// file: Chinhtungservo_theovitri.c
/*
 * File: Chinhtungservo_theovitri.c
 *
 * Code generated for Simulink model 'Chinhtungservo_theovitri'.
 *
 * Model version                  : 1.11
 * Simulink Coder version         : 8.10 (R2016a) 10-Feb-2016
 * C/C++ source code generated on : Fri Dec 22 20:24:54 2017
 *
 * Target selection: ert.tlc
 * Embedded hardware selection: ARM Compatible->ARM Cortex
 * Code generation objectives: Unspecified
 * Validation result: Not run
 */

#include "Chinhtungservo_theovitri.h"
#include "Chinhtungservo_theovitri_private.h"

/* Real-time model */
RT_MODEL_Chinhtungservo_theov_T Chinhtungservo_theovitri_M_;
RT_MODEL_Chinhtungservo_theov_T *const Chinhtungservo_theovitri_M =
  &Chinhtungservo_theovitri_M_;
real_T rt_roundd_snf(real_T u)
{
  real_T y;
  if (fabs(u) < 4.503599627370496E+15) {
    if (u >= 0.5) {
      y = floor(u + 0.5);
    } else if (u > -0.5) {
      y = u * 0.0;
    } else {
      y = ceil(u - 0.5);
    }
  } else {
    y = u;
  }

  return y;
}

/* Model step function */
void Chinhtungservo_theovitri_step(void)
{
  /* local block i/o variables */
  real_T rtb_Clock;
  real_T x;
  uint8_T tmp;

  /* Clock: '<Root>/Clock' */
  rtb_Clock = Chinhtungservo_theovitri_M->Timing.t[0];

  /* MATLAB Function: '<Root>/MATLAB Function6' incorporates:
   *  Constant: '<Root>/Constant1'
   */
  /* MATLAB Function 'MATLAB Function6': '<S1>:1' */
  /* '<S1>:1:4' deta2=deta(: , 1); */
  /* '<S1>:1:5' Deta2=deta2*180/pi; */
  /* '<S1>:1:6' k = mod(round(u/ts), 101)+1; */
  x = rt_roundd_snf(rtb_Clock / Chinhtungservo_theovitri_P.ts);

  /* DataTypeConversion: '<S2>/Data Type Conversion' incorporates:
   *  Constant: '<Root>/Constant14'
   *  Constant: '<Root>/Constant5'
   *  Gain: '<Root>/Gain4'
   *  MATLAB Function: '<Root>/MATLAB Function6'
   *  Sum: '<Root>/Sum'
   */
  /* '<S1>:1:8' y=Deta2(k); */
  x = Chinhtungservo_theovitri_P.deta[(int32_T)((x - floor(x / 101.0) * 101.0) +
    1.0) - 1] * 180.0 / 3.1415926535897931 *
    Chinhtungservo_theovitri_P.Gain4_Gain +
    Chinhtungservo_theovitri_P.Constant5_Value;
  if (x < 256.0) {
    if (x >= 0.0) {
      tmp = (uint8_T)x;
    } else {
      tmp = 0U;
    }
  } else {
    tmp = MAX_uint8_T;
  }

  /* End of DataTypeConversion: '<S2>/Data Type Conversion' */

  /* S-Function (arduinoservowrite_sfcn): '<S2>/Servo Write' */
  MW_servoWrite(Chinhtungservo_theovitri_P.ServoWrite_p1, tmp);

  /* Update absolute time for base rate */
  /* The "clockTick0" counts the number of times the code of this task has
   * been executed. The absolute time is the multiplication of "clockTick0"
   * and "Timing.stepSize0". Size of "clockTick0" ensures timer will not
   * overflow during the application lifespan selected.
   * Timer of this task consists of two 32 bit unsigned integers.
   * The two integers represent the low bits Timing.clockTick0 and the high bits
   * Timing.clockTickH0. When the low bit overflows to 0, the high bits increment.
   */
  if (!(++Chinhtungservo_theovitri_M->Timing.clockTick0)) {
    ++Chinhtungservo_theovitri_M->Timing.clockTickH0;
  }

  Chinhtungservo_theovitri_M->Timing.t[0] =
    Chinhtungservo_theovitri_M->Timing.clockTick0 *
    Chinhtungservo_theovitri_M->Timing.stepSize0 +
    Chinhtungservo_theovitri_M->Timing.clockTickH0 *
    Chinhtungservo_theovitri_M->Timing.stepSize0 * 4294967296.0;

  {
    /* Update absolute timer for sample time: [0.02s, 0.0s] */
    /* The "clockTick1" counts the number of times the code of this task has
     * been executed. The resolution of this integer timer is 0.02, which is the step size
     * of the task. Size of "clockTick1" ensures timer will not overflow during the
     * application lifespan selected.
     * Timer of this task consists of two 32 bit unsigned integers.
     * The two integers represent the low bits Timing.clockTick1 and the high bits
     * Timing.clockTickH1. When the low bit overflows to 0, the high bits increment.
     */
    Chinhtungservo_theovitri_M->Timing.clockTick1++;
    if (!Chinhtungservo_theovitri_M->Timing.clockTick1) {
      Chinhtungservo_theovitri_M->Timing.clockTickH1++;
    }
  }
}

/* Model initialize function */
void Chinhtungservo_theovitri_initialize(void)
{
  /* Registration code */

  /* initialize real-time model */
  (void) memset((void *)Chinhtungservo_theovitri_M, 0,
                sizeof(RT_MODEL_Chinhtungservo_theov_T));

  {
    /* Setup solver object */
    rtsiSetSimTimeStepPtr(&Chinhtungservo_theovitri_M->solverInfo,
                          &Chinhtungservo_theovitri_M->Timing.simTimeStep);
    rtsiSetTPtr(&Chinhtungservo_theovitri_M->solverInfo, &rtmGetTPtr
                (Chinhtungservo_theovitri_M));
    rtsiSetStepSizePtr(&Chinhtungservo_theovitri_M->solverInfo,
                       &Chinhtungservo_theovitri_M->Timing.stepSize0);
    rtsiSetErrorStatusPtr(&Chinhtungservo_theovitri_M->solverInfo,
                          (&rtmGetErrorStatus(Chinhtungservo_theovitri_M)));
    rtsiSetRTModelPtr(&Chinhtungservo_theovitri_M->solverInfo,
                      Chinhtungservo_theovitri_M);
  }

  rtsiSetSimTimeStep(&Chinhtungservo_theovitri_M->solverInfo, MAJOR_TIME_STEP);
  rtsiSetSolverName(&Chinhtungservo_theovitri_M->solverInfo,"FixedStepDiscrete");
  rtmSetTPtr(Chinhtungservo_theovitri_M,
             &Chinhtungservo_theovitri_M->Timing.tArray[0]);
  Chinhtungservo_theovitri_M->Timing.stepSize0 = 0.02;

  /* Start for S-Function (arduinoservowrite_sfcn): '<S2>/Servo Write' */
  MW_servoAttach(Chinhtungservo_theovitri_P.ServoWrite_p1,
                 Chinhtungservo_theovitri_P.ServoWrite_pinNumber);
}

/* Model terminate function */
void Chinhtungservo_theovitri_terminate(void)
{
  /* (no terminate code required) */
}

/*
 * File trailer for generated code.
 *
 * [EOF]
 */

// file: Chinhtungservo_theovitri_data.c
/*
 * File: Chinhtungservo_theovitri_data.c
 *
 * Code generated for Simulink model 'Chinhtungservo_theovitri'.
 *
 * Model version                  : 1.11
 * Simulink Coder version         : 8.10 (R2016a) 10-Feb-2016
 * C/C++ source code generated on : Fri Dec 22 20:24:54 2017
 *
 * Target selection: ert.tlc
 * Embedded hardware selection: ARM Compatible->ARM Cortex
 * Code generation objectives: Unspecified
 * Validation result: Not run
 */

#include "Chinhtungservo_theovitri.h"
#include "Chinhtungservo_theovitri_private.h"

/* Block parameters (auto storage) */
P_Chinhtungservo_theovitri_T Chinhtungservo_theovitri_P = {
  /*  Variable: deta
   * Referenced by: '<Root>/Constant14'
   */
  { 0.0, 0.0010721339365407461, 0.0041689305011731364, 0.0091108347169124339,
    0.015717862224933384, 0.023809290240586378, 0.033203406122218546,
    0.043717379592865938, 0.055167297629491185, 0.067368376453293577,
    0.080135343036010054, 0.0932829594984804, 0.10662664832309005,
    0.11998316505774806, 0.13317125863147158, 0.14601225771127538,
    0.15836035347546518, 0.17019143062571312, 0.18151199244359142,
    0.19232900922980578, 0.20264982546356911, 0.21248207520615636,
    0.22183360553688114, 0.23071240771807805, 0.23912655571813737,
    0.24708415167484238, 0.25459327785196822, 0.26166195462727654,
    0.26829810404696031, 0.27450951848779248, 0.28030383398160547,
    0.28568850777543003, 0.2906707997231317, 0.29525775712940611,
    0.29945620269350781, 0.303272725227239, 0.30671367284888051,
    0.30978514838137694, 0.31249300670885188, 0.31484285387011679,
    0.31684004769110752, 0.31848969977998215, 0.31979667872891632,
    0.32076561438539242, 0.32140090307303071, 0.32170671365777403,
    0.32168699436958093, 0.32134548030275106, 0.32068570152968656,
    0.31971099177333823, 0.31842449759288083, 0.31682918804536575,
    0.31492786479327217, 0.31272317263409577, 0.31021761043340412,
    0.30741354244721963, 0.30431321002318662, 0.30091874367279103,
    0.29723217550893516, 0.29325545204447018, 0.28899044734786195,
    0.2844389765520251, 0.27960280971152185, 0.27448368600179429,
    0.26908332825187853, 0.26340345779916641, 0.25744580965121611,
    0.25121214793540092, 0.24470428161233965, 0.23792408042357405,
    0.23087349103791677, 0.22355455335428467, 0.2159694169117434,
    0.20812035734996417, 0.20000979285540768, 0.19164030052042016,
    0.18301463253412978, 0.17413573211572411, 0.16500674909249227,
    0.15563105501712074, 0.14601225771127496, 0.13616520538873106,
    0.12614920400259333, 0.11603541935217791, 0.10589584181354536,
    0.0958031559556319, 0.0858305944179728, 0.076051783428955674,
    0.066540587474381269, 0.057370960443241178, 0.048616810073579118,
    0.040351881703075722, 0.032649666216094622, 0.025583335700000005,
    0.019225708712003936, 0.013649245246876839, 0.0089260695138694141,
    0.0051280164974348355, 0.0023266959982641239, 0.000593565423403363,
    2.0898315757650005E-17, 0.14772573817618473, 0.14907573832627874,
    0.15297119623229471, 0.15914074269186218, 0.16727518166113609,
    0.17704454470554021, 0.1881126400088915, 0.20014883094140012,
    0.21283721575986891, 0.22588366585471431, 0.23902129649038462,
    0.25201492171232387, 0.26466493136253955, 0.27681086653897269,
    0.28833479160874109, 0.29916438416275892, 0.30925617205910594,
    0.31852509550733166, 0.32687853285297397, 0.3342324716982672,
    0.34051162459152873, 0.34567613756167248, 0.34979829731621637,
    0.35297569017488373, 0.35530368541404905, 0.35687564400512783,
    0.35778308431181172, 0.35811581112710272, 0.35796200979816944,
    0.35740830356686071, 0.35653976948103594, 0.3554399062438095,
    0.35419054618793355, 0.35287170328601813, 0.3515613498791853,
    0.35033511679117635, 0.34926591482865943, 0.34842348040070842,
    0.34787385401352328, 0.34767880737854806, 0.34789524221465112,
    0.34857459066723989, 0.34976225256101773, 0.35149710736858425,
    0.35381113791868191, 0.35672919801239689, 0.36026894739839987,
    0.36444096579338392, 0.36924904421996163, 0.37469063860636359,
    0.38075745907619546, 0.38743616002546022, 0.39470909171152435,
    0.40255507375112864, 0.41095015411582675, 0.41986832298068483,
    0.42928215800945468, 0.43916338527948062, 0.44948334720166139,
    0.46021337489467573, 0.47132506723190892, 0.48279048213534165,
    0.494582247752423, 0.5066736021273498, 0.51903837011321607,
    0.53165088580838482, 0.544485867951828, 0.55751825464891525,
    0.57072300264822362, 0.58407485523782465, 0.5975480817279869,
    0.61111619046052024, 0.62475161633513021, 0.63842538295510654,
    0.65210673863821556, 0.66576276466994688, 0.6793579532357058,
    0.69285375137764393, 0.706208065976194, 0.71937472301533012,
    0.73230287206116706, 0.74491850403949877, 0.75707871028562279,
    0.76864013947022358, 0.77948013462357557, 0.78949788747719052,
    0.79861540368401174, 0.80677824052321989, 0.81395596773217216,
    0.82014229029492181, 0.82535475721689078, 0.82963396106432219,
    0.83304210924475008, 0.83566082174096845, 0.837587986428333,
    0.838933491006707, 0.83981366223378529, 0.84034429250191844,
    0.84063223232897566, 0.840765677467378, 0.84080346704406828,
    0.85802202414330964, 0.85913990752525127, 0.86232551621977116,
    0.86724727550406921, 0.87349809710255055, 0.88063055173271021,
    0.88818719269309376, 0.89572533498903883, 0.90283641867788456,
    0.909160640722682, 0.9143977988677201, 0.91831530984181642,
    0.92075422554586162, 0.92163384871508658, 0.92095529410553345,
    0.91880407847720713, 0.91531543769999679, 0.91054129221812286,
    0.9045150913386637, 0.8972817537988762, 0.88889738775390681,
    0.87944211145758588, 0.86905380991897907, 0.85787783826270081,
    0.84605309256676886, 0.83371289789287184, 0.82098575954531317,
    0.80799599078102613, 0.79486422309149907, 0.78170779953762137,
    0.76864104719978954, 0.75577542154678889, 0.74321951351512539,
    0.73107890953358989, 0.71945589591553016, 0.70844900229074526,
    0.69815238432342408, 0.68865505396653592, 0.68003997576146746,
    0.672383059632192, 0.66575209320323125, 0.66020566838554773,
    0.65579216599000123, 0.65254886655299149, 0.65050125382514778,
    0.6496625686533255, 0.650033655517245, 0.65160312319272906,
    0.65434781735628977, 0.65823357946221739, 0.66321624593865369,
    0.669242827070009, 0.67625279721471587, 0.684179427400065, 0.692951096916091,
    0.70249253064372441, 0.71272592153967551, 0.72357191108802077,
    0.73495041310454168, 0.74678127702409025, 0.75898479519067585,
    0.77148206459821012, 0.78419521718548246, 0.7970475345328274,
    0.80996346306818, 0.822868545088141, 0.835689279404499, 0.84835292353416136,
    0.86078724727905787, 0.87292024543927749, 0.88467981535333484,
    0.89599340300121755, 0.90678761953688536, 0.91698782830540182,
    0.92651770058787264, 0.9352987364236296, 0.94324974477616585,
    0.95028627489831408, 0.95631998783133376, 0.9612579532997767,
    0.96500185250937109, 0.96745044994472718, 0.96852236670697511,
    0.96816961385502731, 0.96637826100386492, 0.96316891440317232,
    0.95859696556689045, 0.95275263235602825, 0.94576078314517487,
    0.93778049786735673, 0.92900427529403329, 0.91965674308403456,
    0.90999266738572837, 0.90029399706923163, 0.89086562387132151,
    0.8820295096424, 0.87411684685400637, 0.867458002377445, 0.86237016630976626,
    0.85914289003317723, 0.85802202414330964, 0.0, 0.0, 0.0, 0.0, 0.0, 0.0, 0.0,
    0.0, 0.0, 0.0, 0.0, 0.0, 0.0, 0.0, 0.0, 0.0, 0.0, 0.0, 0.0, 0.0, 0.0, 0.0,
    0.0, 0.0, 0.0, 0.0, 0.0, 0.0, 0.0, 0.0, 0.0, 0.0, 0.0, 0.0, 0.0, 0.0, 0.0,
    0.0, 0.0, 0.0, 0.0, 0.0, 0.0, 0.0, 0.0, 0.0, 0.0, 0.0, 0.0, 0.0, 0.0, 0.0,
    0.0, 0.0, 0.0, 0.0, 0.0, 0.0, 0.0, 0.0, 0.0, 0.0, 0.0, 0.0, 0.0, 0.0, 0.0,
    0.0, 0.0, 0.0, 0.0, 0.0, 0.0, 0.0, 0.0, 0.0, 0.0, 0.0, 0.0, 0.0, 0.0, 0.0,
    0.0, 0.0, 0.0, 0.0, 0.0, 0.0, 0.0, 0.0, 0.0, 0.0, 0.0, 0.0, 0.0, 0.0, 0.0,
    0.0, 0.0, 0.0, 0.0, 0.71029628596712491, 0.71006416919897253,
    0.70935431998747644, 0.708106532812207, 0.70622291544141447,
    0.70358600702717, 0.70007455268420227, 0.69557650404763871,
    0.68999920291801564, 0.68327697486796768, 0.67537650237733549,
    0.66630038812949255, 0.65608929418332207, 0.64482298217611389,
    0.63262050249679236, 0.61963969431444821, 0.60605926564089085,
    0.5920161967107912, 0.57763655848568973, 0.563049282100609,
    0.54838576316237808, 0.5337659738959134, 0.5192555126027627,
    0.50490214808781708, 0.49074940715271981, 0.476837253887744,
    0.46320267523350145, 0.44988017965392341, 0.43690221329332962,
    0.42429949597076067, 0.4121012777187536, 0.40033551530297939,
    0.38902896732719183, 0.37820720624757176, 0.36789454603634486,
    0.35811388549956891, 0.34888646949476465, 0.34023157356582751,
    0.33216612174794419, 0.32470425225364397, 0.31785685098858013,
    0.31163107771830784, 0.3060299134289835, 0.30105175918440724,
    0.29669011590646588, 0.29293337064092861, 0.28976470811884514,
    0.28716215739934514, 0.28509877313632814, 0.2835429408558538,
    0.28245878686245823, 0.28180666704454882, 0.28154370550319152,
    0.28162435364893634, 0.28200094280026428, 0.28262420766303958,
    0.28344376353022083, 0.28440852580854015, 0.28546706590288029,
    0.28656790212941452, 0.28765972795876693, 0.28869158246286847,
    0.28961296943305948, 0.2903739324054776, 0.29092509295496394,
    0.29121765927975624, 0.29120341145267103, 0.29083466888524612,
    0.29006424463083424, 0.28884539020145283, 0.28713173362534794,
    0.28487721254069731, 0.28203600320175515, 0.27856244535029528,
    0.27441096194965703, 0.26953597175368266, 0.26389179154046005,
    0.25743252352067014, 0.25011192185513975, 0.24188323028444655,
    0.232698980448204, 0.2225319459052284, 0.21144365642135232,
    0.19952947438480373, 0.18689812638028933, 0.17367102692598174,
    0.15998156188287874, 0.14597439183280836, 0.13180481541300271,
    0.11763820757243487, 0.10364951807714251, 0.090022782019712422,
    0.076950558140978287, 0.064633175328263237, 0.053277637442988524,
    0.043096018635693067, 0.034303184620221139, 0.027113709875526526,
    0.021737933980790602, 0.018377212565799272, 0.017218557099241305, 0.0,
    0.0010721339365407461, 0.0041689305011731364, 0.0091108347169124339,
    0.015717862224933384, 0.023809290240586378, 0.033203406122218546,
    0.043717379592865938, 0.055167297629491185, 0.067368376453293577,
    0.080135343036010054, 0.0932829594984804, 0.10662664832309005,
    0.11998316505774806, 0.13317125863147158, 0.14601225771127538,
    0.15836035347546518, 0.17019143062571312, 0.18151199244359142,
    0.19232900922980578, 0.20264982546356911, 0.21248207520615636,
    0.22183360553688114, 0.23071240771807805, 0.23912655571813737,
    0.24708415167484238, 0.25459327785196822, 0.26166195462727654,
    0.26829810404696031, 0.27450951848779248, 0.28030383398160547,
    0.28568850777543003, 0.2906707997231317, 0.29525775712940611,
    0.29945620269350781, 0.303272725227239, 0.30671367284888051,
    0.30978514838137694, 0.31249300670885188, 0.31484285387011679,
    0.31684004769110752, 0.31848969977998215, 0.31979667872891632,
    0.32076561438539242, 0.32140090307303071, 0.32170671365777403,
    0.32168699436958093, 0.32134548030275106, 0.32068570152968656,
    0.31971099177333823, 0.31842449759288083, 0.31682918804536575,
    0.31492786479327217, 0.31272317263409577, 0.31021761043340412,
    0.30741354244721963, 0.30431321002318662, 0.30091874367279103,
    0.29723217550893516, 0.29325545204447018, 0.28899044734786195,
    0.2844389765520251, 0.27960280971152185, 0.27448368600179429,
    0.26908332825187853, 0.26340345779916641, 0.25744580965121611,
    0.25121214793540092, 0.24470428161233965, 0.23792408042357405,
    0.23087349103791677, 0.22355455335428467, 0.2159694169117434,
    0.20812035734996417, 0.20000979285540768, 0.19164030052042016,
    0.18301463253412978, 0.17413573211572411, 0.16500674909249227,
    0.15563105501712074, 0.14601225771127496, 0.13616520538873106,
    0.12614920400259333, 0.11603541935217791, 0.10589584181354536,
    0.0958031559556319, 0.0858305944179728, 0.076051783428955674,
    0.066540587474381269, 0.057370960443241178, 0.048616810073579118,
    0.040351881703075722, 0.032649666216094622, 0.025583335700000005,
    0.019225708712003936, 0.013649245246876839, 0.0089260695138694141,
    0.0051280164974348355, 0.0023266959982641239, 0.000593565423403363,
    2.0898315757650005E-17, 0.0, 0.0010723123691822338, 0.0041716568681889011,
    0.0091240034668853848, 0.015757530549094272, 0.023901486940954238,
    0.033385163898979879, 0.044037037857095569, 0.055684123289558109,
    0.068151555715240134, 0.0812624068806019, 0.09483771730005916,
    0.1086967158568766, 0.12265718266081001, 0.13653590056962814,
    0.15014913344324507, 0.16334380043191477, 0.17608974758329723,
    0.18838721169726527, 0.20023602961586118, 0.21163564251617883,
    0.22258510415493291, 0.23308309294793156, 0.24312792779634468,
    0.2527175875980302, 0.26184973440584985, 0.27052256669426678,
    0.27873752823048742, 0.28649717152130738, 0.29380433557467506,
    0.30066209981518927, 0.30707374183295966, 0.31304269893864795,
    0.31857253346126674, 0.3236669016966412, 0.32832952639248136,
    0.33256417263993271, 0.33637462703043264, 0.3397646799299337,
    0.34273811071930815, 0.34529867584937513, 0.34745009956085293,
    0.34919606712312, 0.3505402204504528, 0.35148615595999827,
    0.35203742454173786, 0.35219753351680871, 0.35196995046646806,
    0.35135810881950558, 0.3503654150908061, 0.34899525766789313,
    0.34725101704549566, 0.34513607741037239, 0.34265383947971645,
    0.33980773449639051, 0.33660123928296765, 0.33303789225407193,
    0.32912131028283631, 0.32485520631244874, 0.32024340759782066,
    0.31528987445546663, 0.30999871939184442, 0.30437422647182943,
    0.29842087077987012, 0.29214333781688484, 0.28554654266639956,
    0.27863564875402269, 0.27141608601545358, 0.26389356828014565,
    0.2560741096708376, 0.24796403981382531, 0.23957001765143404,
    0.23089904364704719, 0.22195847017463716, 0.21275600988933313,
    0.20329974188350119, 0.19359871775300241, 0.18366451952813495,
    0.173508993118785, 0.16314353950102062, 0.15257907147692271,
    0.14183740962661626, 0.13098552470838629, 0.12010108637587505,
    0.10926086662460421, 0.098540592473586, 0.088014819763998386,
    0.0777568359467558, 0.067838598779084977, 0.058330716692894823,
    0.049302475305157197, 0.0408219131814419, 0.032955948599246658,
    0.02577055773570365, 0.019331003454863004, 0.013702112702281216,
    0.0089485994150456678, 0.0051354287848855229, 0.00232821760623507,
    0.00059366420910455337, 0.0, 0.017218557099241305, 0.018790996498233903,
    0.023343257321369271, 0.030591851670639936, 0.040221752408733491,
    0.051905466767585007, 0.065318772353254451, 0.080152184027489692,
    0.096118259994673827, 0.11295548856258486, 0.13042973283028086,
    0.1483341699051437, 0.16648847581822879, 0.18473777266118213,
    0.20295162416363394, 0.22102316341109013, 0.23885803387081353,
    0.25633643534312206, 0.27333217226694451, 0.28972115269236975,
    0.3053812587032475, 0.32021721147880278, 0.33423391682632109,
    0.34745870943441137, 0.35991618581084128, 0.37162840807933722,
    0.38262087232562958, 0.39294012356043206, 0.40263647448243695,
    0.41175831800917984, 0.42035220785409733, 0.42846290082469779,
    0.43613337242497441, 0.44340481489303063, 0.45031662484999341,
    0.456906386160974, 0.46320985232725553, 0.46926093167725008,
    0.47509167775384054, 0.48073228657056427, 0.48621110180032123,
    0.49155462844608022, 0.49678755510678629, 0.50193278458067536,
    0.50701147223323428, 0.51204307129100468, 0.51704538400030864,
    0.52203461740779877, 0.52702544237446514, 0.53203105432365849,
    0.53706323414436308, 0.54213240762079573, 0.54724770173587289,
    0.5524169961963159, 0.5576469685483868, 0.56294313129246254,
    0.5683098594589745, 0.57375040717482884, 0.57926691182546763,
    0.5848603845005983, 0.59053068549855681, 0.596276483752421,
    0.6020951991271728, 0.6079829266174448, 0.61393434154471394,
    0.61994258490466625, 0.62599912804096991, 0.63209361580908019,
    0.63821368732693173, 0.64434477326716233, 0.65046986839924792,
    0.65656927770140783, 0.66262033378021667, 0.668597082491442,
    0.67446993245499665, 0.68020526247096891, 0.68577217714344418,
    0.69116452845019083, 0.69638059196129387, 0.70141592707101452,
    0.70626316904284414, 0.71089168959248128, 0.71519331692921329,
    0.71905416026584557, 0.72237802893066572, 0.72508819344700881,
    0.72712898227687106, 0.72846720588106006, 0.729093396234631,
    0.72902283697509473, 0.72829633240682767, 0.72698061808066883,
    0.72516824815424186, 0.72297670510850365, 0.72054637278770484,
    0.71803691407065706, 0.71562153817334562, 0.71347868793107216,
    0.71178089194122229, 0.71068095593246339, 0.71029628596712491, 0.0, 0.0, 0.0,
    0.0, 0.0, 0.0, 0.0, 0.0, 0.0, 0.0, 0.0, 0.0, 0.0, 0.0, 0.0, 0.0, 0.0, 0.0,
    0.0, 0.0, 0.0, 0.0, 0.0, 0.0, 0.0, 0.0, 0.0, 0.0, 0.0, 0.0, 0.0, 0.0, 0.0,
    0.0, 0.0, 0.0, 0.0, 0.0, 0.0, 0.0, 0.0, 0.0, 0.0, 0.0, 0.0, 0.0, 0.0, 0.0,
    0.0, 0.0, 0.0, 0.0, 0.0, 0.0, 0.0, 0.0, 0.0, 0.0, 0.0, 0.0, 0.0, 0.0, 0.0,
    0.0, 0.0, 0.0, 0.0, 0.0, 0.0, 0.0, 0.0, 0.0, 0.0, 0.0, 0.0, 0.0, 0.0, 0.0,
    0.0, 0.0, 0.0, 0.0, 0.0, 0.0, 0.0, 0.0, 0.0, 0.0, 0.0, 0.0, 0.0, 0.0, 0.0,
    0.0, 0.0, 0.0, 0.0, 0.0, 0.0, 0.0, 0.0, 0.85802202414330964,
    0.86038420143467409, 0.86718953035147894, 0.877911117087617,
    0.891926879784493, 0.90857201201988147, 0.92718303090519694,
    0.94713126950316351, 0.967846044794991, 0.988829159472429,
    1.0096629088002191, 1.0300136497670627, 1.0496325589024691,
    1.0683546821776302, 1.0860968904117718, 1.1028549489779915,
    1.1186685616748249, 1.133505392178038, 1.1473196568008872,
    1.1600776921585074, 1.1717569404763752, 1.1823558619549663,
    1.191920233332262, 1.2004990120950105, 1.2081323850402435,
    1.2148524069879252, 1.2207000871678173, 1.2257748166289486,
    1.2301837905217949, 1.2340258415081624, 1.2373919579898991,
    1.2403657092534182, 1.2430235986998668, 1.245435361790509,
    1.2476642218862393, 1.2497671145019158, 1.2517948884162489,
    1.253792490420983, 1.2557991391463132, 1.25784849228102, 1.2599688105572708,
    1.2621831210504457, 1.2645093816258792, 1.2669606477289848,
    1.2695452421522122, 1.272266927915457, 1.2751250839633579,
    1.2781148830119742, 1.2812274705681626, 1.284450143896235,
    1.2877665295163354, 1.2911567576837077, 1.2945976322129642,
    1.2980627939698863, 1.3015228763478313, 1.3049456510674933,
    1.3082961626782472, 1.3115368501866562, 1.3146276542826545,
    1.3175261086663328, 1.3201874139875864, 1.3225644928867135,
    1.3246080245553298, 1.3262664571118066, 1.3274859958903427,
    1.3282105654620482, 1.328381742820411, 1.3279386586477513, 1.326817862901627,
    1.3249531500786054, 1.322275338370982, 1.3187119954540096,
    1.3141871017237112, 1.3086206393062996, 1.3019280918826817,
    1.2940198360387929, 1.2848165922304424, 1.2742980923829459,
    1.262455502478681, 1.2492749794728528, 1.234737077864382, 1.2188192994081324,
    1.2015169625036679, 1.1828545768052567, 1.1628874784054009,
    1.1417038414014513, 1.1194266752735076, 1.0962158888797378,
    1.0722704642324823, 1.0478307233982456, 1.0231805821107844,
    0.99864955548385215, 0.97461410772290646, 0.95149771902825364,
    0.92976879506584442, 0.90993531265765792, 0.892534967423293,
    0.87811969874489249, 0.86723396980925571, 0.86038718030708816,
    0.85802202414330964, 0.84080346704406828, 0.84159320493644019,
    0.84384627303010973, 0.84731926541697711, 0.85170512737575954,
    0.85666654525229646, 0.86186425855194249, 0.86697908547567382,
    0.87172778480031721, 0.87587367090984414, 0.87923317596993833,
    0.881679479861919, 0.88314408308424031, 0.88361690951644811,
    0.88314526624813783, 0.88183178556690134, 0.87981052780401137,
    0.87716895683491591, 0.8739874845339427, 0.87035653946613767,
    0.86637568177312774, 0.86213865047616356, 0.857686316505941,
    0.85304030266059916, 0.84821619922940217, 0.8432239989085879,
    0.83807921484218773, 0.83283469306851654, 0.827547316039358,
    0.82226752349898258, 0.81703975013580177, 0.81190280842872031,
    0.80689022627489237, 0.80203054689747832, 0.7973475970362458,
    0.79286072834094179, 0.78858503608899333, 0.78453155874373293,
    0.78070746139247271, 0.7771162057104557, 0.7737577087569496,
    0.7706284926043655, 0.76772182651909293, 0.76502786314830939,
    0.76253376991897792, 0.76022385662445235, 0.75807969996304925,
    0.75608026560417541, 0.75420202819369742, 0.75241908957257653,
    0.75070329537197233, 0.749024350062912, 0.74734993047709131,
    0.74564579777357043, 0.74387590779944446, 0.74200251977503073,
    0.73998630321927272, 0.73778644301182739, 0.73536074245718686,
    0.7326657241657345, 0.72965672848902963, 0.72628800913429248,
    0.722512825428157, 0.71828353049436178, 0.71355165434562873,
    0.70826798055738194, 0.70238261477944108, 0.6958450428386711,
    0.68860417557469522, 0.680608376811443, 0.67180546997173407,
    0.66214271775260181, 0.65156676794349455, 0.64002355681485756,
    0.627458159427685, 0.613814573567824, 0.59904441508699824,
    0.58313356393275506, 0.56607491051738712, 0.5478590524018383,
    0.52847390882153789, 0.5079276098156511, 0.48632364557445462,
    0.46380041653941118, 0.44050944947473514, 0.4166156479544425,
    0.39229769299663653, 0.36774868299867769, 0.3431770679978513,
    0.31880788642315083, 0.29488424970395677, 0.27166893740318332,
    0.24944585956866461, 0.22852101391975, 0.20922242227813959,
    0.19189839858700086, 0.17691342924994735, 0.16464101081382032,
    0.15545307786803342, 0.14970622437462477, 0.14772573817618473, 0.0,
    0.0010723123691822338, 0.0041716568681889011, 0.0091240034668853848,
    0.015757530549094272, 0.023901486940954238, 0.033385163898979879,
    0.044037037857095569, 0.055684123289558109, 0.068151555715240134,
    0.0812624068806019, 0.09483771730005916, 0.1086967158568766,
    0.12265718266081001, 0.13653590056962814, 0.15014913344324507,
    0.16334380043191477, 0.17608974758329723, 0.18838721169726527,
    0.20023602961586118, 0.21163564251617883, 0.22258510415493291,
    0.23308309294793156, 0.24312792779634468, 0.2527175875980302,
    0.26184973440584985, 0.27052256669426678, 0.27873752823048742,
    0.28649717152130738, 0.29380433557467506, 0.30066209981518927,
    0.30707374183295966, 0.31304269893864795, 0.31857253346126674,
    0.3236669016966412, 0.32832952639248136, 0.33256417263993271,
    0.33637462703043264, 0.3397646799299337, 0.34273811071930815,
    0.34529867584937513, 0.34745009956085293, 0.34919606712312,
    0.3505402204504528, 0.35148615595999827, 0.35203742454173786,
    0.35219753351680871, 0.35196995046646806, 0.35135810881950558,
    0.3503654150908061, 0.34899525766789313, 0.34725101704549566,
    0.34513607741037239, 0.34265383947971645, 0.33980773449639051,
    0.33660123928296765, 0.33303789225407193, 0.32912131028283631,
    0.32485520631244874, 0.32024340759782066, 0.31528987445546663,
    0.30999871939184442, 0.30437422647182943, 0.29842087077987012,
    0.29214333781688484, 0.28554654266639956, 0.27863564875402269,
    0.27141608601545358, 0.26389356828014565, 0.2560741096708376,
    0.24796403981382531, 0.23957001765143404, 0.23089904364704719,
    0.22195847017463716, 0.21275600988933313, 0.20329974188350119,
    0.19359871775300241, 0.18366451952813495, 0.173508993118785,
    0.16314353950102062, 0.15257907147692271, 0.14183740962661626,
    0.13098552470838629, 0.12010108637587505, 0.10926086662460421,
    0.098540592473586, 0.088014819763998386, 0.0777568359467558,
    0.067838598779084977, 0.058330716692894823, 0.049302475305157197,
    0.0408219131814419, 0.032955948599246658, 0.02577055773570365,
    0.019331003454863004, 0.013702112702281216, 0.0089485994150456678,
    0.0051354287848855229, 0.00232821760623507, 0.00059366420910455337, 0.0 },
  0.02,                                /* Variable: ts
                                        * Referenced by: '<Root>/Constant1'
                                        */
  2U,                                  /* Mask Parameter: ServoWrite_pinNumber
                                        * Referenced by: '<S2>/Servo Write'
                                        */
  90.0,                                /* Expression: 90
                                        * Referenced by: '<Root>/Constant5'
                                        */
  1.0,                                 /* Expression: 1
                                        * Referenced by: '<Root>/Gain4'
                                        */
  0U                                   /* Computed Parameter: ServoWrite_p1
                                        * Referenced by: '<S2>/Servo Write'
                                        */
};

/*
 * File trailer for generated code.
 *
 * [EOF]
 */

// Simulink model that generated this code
simulink model "Chinhtungservo_theovitri"  (R2016a)
settings: Solver=FixedStepDiscrete  StartTime=0.0  StopTime=inf  FixedStep=0.02  RelTol=1e-3
InitFcn:
  | ts = 0.02;
values from neighbouring files (symbols this model uses):
  deta = [0 0.00107213393654 0.00416893050117 0.00911083471691 0.0157178622249 0.0238092902406 0.0332034061222 0.0437173795929 0.0551672976295 0.0673683764533 0.080135343036 0.0932829594985 ... (1212 elements, 101x12)]    [dang1.mat]    (also in dang3.mat = [0 0.00112687810751 0.00436390592225 0.00949550865103 0.0163; dang4.mat = [0 0.00183366934445 0.00704247991907 0.015187473155 0.025827)
libraries: arduinolib x1

== system Chinhtungservo_theovitri ==
  Clock : Clock
  Constant1 : Constant  Value=ts  SampleTime=0.02
  Constant14 : Constant  Value=deta
  Constant5 : Constant  Value=90  SampleTime=0.02
  Gain4 : Gain
  MATLAB Function6 : MATLAB Function  TreatAsAtomicUnit=on
  Standard Servo Write5 : arduinolib/Standard Servo Write  pinNumber=2  blockPlatform=arduino
  Sum : Sum  Inputs=|++
  wires:
  Sum/1 -> Standard Servo Write5/1
  Constant5/1 -> Sum/1
  Gain4/1 -> Sum/2
  MATLAB Function6/1(y) -> Gain4/1
  Constant14/1 -> MATLAB Function6/2(deta)
  Constant1/1 -> MATLAB Function6/3(ts)
  Clock/1 -> MATLAB Function6/1(u)

== matlab function Chinhtungservo_theovitri/MATLAB Function6 ==
function y = fcn(u,deta,ts)
%#codegen

deta2=deta(: , 1);
Deta2=deta2*180/pi;
k = mod(round(u/ts), 101)+1;

y=Deta2(k);
